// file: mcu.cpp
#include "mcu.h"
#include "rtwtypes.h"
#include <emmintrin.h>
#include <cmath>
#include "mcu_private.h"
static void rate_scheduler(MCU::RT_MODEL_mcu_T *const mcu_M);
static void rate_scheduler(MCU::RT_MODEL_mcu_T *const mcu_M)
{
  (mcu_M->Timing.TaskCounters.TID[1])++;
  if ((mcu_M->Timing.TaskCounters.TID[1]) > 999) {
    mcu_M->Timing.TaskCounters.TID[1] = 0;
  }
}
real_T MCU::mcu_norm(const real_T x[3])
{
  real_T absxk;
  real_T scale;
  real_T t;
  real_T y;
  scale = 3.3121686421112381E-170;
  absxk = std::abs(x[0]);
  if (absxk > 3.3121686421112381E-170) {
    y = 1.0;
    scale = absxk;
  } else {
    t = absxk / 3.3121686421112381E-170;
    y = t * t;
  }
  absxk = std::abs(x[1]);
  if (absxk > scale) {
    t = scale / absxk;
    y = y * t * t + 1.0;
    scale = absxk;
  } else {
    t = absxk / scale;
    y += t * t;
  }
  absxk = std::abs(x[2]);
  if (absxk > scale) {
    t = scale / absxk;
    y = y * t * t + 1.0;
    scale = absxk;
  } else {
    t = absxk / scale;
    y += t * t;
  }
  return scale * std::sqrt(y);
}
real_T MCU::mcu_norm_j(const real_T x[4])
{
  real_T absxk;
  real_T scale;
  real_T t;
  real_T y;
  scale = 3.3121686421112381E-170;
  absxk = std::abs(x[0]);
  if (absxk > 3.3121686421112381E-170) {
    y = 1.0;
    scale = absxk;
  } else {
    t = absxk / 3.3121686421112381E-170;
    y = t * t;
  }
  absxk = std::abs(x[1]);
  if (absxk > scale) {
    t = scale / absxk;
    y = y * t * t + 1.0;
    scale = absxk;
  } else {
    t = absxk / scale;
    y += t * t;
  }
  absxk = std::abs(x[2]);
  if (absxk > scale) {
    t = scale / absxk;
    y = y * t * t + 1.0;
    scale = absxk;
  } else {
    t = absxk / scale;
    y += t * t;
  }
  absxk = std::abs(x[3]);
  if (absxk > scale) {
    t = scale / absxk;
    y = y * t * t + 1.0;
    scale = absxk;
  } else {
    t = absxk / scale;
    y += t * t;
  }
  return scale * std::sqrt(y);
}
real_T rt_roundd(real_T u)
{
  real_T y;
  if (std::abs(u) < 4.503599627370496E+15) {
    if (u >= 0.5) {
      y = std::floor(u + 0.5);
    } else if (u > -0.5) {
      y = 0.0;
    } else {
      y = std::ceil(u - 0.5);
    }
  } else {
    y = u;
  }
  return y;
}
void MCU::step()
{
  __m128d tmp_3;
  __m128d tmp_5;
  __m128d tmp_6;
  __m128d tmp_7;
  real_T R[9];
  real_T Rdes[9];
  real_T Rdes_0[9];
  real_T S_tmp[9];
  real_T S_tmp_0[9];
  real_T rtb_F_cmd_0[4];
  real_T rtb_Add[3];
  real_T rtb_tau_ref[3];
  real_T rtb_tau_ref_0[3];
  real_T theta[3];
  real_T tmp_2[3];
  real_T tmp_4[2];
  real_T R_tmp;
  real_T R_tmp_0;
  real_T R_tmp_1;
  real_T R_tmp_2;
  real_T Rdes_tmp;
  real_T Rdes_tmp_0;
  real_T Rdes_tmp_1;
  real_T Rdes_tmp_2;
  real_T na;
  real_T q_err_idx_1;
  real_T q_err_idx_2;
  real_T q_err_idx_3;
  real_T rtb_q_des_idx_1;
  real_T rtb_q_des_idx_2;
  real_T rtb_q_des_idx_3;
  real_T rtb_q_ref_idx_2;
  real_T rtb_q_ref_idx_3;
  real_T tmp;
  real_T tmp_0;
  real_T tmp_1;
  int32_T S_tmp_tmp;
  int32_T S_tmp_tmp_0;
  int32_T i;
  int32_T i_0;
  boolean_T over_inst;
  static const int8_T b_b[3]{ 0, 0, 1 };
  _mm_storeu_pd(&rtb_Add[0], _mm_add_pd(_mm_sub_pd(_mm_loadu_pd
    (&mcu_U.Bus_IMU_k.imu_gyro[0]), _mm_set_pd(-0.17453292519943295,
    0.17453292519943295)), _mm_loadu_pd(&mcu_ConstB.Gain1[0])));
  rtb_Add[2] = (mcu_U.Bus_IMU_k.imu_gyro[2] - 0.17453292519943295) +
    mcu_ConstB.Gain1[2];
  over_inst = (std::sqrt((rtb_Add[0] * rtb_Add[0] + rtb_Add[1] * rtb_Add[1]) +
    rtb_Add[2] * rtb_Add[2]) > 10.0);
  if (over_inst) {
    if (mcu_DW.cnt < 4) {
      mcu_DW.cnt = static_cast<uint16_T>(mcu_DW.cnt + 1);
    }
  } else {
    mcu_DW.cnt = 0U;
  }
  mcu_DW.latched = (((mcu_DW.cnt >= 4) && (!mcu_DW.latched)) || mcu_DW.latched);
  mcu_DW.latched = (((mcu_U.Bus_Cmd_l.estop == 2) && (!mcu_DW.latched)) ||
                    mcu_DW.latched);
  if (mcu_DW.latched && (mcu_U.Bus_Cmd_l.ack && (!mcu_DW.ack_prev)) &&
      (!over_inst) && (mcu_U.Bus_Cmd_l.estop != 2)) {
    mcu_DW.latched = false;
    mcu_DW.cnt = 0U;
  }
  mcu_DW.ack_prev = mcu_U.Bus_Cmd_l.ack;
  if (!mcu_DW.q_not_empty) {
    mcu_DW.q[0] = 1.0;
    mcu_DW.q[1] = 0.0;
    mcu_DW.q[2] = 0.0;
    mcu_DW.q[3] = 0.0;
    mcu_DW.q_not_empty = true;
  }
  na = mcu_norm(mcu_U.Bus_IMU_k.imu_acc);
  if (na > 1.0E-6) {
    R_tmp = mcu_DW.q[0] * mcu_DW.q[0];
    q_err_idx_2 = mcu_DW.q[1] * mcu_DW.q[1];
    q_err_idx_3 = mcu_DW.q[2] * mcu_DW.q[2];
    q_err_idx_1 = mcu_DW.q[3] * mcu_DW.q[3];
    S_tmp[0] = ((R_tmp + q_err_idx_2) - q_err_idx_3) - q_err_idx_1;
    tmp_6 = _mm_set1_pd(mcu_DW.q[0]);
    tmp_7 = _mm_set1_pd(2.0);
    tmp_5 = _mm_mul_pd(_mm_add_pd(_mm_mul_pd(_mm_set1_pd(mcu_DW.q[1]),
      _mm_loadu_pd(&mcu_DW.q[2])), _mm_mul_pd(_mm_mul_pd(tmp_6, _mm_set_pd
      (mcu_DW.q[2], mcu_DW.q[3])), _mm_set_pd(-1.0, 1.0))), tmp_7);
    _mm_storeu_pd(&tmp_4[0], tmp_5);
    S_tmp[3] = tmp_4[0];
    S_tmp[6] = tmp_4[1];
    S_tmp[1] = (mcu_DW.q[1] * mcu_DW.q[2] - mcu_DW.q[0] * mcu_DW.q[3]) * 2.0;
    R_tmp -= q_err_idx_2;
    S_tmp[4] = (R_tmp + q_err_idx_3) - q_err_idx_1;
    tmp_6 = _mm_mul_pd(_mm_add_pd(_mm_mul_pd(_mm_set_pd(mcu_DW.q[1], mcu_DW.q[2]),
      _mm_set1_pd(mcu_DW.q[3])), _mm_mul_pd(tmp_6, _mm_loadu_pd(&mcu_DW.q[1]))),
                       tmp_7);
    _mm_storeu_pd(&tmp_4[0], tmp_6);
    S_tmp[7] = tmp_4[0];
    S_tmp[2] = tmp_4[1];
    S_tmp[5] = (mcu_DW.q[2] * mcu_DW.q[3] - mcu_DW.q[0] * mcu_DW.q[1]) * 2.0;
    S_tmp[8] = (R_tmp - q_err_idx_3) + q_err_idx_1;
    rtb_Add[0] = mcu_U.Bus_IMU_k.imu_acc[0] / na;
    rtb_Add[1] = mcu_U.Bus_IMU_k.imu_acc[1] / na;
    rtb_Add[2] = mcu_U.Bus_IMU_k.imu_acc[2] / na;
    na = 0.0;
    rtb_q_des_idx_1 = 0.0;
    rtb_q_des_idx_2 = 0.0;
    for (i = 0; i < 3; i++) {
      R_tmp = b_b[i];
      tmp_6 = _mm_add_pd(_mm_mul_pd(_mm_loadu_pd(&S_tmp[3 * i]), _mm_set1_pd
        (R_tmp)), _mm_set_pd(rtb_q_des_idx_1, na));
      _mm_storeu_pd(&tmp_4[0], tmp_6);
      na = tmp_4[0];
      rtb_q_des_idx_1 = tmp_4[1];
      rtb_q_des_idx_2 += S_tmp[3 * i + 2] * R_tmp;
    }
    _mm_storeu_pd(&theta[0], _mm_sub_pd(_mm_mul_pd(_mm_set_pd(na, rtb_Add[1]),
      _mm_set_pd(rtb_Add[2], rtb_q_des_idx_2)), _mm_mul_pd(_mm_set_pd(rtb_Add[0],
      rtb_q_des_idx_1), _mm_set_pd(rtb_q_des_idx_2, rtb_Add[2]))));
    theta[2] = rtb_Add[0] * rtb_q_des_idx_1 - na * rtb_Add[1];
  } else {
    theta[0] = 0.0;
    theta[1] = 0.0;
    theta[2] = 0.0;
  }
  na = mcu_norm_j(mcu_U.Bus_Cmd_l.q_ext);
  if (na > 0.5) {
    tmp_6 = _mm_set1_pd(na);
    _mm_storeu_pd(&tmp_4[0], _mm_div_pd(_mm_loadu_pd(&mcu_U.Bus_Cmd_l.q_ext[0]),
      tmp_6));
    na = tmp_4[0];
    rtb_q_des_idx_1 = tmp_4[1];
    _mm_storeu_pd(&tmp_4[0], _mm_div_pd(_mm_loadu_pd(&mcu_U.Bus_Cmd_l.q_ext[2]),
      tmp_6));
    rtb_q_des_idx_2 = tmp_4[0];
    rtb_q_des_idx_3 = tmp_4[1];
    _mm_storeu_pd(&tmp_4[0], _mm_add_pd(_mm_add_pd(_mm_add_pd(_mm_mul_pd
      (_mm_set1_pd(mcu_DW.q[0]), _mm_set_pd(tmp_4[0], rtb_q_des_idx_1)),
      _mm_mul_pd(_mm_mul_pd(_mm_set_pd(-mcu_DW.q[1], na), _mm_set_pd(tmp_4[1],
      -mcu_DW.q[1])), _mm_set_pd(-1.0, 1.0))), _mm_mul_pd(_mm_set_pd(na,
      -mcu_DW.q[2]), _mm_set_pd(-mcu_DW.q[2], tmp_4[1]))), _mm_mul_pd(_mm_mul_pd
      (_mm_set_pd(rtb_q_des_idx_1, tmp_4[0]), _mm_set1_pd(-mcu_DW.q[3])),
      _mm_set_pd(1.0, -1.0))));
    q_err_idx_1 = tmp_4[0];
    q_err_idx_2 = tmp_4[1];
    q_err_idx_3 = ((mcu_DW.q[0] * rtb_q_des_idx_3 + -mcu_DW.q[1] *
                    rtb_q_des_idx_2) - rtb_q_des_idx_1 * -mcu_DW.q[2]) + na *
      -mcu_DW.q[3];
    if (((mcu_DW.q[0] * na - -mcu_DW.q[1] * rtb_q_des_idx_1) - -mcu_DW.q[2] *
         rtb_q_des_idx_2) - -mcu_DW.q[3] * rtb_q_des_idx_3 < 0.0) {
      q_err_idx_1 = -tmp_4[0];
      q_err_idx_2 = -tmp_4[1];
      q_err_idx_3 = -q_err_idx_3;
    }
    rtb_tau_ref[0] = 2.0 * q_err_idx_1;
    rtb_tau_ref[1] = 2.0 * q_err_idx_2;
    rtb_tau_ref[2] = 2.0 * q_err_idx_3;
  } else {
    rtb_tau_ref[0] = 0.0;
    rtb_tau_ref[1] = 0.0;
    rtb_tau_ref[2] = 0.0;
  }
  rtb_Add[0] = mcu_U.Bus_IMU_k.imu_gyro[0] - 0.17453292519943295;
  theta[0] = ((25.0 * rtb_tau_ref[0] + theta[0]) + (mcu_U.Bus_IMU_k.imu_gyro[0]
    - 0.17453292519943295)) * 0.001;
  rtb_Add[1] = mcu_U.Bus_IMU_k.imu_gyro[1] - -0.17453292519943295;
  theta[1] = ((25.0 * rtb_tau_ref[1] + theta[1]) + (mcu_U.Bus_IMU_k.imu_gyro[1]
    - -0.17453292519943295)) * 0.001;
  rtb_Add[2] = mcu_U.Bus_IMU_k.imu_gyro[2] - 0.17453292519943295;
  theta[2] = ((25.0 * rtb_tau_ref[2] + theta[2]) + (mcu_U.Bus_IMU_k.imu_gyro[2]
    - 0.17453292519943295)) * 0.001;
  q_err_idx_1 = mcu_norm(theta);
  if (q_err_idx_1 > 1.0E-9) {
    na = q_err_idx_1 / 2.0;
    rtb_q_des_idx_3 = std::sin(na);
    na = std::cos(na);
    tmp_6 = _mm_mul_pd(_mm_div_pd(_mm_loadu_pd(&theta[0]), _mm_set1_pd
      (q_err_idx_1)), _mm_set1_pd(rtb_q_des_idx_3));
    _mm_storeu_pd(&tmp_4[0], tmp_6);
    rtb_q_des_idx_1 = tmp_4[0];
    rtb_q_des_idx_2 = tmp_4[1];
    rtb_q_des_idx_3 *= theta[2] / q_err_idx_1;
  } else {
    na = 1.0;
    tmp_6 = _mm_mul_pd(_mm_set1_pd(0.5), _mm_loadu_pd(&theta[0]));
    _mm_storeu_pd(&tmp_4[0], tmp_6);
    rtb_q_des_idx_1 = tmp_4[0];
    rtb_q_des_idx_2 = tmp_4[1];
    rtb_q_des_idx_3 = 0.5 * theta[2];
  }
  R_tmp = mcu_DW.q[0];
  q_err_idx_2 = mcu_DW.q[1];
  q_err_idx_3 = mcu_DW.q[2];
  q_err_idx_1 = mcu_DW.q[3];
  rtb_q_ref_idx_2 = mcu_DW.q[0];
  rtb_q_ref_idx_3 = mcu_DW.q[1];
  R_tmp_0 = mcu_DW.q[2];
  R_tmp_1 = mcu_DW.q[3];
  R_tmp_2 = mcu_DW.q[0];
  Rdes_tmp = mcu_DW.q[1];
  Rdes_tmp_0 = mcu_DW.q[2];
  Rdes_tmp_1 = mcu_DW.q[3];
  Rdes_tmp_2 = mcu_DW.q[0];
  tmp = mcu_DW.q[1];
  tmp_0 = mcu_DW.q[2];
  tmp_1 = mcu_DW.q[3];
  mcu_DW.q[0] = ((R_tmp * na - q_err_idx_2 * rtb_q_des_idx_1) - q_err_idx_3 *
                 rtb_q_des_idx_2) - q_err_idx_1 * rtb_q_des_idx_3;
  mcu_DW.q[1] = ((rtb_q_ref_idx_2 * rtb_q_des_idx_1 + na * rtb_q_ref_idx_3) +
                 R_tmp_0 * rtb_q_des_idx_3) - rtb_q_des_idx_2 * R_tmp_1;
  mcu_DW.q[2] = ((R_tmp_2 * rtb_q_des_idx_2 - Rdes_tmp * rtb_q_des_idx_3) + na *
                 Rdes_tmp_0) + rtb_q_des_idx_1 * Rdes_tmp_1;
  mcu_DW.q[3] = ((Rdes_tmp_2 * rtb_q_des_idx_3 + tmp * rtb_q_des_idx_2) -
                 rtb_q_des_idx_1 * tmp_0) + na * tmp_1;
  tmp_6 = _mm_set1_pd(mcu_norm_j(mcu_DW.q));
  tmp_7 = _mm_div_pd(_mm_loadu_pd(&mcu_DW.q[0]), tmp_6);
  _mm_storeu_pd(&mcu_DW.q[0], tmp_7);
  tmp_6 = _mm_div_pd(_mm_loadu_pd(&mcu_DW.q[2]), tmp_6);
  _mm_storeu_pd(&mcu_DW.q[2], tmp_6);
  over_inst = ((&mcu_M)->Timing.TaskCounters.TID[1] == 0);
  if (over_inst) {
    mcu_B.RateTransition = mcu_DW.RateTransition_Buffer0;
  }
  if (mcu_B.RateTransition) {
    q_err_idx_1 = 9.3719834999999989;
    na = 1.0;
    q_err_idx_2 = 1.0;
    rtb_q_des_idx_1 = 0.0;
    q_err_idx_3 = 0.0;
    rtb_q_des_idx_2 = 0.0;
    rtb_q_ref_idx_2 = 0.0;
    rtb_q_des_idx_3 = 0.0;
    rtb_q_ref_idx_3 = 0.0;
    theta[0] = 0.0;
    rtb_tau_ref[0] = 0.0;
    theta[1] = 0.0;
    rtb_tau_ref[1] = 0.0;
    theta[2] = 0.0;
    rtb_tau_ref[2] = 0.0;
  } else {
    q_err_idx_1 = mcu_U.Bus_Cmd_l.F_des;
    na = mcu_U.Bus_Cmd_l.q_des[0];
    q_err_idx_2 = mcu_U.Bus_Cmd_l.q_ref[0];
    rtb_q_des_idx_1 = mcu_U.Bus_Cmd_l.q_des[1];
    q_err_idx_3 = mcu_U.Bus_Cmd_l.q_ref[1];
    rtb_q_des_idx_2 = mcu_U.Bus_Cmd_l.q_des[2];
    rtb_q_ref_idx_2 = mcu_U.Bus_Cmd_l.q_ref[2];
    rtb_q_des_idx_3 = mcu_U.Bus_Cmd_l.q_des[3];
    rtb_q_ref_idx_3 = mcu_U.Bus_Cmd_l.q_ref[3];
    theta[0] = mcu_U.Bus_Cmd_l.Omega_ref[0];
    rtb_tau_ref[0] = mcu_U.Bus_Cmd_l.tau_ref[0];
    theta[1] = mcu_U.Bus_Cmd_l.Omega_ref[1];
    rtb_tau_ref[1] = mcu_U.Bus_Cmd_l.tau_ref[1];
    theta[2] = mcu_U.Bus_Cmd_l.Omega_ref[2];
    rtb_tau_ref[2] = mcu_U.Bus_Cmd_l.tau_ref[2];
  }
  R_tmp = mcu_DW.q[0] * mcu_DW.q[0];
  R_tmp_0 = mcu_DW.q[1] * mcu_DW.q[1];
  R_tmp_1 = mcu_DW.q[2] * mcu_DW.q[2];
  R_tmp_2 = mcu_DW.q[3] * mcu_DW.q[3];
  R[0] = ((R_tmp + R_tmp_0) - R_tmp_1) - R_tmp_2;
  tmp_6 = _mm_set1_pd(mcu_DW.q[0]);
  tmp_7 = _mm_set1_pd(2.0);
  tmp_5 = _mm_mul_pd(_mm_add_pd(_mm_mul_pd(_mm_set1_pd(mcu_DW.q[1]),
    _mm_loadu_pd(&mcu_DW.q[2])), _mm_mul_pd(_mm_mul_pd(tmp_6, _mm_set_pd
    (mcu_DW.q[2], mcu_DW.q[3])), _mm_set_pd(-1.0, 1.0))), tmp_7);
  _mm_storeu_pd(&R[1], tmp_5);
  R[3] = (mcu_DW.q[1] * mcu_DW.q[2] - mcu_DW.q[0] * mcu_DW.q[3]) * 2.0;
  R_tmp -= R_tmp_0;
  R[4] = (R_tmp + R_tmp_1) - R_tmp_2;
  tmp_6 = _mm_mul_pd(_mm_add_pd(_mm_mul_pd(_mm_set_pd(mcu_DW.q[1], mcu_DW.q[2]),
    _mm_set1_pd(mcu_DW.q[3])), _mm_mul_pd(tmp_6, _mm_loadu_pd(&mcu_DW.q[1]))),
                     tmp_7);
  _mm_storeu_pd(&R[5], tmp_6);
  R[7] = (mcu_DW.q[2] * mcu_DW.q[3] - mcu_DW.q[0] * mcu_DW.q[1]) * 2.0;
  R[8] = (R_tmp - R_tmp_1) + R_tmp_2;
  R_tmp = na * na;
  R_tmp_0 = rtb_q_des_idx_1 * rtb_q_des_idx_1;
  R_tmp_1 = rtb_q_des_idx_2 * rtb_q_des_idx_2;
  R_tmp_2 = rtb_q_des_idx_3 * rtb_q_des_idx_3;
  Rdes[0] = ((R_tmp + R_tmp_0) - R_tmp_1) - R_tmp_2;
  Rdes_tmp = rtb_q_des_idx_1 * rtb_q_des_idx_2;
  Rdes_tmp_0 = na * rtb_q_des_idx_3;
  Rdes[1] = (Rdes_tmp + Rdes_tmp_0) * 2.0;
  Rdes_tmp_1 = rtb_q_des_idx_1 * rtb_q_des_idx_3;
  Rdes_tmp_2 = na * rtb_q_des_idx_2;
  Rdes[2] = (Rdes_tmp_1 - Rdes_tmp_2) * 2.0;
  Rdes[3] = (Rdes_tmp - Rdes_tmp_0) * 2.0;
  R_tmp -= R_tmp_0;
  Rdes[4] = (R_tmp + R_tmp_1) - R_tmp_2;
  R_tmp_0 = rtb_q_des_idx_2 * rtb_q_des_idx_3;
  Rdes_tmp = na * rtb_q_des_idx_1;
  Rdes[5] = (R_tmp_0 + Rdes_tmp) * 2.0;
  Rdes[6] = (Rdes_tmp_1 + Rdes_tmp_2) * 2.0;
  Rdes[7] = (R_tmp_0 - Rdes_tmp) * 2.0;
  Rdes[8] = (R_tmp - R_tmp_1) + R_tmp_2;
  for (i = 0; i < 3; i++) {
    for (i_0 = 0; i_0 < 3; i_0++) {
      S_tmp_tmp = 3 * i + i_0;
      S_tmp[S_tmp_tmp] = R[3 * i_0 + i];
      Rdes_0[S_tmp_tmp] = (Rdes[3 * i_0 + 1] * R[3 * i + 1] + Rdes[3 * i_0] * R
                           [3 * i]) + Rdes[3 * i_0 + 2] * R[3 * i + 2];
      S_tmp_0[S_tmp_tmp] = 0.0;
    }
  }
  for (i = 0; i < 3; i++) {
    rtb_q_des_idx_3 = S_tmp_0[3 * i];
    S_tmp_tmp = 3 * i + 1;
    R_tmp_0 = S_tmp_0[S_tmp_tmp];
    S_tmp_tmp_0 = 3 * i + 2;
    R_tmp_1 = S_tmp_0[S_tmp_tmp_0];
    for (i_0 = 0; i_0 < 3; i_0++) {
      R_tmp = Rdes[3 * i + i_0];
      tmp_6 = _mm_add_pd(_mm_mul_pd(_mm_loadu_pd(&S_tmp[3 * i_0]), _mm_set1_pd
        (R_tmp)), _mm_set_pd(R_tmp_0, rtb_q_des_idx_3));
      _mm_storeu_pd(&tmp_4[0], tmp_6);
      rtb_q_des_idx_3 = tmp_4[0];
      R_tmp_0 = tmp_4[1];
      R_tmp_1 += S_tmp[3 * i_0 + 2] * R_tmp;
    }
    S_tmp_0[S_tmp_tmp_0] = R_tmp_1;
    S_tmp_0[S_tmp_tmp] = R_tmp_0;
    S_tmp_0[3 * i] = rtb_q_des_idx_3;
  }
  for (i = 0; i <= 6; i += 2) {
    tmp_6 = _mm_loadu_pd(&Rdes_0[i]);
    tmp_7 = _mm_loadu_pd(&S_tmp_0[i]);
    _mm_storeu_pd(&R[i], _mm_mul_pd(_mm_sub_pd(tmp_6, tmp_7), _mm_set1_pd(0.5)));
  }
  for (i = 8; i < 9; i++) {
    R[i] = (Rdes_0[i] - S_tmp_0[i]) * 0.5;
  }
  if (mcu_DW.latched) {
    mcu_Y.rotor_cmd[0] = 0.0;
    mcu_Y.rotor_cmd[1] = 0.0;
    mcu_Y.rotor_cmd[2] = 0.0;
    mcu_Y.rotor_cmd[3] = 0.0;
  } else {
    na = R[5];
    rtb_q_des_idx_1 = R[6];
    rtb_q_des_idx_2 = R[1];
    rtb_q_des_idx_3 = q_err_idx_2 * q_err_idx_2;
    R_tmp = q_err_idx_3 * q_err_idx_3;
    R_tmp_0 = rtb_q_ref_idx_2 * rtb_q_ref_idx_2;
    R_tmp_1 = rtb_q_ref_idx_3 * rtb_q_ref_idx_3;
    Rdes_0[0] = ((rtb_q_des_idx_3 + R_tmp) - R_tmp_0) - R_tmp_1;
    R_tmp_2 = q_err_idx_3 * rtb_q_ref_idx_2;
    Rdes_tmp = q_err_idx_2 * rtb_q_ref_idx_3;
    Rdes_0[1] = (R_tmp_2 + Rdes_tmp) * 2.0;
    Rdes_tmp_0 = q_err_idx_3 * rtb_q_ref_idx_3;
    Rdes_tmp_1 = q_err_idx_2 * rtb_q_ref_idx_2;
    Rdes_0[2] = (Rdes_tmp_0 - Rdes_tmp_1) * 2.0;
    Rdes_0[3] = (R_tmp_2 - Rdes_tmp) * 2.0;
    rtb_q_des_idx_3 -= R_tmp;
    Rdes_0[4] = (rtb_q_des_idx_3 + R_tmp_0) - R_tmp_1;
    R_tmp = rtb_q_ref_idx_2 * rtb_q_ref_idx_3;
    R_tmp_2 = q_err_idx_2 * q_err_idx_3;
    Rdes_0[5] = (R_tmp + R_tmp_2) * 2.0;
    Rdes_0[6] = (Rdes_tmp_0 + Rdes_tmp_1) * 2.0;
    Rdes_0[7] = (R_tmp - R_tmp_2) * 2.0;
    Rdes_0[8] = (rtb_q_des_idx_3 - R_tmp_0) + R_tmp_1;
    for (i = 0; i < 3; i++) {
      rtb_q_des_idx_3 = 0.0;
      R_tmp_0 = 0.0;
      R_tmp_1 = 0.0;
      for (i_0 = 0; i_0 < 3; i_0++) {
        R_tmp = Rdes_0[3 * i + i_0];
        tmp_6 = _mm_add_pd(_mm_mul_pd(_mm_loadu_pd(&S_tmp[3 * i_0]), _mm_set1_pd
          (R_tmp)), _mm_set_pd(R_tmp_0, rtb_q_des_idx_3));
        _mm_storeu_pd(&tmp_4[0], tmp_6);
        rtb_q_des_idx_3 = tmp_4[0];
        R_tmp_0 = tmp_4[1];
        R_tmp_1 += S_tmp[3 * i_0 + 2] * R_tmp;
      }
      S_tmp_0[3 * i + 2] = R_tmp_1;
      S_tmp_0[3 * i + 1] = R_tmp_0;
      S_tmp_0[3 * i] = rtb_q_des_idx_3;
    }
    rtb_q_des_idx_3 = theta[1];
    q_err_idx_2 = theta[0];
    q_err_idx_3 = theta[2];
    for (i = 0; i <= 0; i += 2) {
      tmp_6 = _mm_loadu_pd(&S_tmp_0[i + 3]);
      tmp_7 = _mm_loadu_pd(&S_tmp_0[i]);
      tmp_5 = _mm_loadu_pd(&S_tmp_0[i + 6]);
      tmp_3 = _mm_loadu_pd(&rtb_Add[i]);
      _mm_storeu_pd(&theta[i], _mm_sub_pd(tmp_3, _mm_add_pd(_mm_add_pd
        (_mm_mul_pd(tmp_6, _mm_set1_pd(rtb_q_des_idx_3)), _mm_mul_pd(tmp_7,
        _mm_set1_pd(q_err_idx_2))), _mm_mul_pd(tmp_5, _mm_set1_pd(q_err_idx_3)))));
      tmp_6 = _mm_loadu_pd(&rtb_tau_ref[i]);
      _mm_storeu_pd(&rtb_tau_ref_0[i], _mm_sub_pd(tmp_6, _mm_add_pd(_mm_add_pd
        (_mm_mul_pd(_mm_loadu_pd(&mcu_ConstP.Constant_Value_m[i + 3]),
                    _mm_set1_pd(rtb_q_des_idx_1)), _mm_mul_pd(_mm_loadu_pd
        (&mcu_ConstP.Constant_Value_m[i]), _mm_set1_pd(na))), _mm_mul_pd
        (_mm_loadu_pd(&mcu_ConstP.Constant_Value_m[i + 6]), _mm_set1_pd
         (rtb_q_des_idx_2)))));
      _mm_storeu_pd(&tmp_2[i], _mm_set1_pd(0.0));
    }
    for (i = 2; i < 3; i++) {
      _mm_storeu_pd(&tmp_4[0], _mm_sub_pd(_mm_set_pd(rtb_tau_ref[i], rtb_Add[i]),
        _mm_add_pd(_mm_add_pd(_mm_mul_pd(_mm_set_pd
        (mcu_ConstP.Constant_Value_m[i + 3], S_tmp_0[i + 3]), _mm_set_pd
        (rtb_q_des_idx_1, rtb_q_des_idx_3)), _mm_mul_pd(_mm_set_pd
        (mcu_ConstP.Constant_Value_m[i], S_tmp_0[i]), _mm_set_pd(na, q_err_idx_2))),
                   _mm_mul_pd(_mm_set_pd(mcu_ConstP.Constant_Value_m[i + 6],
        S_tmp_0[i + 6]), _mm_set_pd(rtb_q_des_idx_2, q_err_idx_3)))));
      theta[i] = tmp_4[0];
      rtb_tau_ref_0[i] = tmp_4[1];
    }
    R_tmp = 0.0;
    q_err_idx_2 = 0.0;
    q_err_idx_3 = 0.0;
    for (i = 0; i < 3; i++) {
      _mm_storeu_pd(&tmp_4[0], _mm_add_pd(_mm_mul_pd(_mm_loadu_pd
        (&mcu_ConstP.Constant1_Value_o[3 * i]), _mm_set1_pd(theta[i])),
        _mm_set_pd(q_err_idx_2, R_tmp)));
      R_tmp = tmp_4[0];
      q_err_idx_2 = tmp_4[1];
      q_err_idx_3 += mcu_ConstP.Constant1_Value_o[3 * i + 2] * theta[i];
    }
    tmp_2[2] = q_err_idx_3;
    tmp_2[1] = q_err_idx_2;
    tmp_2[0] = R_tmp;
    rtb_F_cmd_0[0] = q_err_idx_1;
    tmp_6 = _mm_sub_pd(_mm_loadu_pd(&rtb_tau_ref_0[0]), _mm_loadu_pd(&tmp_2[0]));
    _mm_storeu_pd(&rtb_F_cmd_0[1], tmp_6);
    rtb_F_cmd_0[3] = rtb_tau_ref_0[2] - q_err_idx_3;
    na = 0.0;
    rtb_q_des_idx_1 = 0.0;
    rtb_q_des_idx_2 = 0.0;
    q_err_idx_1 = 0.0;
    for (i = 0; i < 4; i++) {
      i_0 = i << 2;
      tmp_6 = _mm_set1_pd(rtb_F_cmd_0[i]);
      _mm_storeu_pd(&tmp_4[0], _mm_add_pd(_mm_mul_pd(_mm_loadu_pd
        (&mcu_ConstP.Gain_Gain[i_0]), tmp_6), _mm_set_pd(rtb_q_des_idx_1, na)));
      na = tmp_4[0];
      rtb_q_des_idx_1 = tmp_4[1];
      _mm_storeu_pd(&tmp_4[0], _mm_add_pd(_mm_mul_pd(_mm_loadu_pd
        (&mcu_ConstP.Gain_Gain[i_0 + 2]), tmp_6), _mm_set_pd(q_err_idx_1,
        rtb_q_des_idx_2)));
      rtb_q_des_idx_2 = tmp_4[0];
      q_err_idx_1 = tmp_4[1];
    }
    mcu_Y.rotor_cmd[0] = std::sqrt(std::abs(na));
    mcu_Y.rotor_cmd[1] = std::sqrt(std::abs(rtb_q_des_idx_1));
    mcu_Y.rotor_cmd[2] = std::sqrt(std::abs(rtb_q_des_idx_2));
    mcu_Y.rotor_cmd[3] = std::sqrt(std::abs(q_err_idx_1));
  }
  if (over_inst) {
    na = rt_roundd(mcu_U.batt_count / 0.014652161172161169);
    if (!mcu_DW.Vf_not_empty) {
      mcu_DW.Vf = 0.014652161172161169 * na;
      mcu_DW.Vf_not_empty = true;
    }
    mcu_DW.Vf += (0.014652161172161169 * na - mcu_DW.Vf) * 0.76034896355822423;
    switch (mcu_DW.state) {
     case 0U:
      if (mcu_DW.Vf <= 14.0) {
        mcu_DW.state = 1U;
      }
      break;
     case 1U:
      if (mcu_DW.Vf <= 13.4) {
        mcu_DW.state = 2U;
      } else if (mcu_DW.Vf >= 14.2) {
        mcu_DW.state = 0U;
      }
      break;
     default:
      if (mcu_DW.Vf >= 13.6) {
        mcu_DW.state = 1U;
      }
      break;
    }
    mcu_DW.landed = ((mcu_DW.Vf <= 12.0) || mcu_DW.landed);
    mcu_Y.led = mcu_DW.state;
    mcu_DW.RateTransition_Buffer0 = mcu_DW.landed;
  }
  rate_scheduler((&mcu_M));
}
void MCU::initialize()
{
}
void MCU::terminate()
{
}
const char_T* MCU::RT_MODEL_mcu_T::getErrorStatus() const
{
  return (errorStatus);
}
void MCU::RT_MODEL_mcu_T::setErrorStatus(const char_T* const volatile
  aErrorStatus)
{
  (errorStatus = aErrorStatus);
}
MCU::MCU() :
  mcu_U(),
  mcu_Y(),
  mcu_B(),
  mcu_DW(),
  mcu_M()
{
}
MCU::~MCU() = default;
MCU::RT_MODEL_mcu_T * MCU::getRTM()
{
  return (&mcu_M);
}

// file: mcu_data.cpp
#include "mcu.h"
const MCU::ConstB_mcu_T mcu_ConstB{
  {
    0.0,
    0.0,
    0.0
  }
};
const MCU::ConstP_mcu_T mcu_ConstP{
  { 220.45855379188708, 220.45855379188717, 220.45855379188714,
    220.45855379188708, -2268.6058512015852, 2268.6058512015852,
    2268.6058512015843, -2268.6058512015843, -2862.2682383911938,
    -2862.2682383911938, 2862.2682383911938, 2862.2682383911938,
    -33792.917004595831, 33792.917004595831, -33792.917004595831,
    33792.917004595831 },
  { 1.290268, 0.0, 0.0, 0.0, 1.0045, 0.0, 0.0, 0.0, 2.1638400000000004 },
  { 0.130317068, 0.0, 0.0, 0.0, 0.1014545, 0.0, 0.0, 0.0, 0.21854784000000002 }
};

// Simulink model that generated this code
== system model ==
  Bus_IMU : Inport
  Bus_Cmd : Inport
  batt_count : Inport
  rotor_cmd : Outport  <- 1: Switch#1
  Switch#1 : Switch  Criteria=u2 > Threshold  <- 1: Constant#1, 2: MATLABFunction#1, 3: Sqrt#1
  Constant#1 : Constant  Value=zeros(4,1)
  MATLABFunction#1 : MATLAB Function  <- 1: Add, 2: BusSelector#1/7, 3: Logic#1
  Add : Sum  <- 1: Sum#1, 2: Gain1
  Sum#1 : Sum  Inputs=+-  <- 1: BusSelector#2, 2: Constant1
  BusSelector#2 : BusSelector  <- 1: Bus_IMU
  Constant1 : Constant  Value=imu.gyro_bias
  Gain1 : Gain  Gain=0  <- 1: Constant#2
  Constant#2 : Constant  Value=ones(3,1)
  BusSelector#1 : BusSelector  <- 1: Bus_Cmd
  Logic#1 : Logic  Operator=OR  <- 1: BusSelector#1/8, 2: Constant#3
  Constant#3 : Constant  Value=0
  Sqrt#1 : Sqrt  <- 1: Abs#1
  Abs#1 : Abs  <- 1: Gain
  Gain : Gain  Gain=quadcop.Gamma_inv  Multiplication=Matrix(K*u) (u vector)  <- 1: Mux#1
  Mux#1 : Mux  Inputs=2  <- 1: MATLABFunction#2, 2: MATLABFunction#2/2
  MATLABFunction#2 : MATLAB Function  <- 1: MATLABFunction#3, 2: MATLABFunction#3/2, 3: MATLABFunction#4, 4: MATLABFunction#4/5, 5: MATLABFunction#4/2, 6: MATLABFunction#4/3, 7: MATLABFunction#4/4, 8: Constant, 9: Constant#4
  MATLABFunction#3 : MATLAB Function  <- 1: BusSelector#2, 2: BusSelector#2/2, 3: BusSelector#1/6, 4: Constant#5, 5: Constant#6, 6: Constant#7, 7: Constant#8, 8: Constant1
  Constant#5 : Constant  Value=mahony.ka
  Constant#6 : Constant  Value=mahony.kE
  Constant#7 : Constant  Value=imu.Ts
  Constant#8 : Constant  Value=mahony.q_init
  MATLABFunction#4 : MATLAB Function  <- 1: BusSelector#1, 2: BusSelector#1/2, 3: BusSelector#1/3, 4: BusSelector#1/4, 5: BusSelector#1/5, 6: RateTransition
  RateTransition : RateTransition  <- 1: MATLABFunction#5/2
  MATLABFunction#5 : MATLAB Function  <- 1: MATLABFunction#6
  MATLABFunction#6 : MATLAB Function  <- 1: batt_count
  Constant : Constant  Value=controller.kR
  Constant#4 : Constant  Value=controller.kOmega
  led : Outport  <- 1: MATLABFunction#5
== matlab function MATLAB Function ==
function [F, tau] = geo_attitude_ctrl(q, Omega, q_des, q_ref, Omega_ref, F_des, tau_ref, kR, kOmega)
%#codegen
% GEO_ATTITUDE_CTRL Geometrischer Lageregler auf SO(3).
%   Lee/Leok/McClamroch (CDC 2010), 2-DOF Error-Feedback:
%       tau = tau_ff - kR*eR - kOmega*eOmega
%
%   ZWEI getrennte Referenzen (NICHT identisch!):
%     q_des : Solllage aus dem Folgeregler pos_ctrl (mit Positionsrueckfuehrung)
%             -> bestimmt den Lagefehler e_R.
%     q_ref : nominelle Solllage aus traj_gen (reine Vorsteuerung)
%             -> Frame, in dem Omega_ref definiert ist ([Om_ref]x = R_ref' R^T_ref)
%             -> Transport von Omega_ref in den aktuellen Body-Frame.
%
%
%   EIN-/AUSGAENGE:
%     q, Omega         : aktuelle Lage/Drehrate
%     q_des            : Solllage aus pos_ctrl
%     q_ref            : Solllage aus traj_gen 
%     Omega_ref        : Vorsteuer-Drehrate im Body-Frame aus traj_gen
%     F_des, tau_ff    : Vorsteuerung Schub/Moment aus traj_gen
%     kR, kOmega       : 3x3-Gains
%     F, tau           : Schubsollwert, Stellmoment

R    = quat2dcm_local(q)';      
Rdes = quat2dcm_local(q_des)';   
Rref = quat2dcm_local(q_ref)';    

% --- Lagefehler gegen die rueckgefuehrte Solllage R_des ---
S  = 0.5*(Rdes'*R - R'*Rdes);     % schiefsymmetrisch
eR = [S(3,2); S(1,3); S(2,1)];    % vee

% --- Drehratenfehler: Omega_ref aus R_ref-Frame in aktuellen Frame transportieren ---
eOmega = Omega - R'*Rref*Omega_ref;

% --- Stellgesetz ---
tau = tau_ref - kR*eR - kOmega*eOmega;
% Optional voll-geometrisch: 
% tau = tau + cross(Omega, J*Omega);

F = F_des;
end

== matlab function MATLAB Function ==
function [q_hat, Omega_hat] = mahony_filter(imu_gyro, imu_acc, q_ext, ka, kE, Ts, q_init, b_ground)
%#codegen
% MAHONY_FILTER  Expliziter Komplementaerfilter auf SO(3), zeitdiskret.
%   Mahony/Hamel/Pflimlin (TAC 2008)). km = 0 (kein Magnetometer)
%
%     - Accel misst spezifische Kraft; im Hover [0;0;-g] -> Richtung
%       v0 = [0;0;-1]. 
%
%   EIN-/AUSGAENGE:
%     imu_gyro [rad/s] (3x1)  : gemessene Koerperdrehrate (mit Bias+Rauschen)
%     imu_acc  [m/s^2] (3x1)  : gemessene spezifische Kraft (Koerper)
%     q_ext    (4x1)          : externe Mocap-Lage 
%     ka, kE, kb (Skalar)     : Tilt-, Externreferenz-, Bias-Gain
%     Ts       [s]            : Abtastperiode 
%     q_init   (4x1)          : Startlage 
%     b_init   (3x1)          : Startbias
%     b_clamp  (Skalar)       : Maximalwert des Bias
%     q_hat    (4x1)          : geschaetzte Lage
%     Omega_hat(3x1)          : bias-korrigierte Drehrate (fuer Lageregler)
%     b_hat    (3x1)          : geschaetzter Gyro-Bias (Diagnose)
%     e_acc    (3x1)          : Innovationsterm zur Diagnose

persistent q
if isempty(q)
    q = q_init; % Startlage
end

% --- 1) Innovation (nur Richtung, Betrag traegt keine Lageinfo) ---
na = norm(imu_acc);
if na > 1e-6
    v_acc = imu_acc / na; % spezifische Kraft DCM_{be}(a -g*[0;0;-1]) in Körperkoordinaten
    v_hat = quatRotate(q, [0; 0; 1]); % geschaetzte Schwerkraftrichtung in Körperkoordinaten
    e_acc = cross(v_acc, v_hat); % Schätzfehler = Innovationsterm
else
    e_acc = [0; 0; 0]; % Freifall = unbrauchbar
end

% --- 2) Externe Mocap-Lage ---
nE = norm(q_ext);
if nE > 0.5
    qe    = q_ext / nE; % normieren da durch Quantisierung/Rauschen q_ext kein Einheitsquaternion
    q_err = quatMul(quatConj(q), qe); % Koerperinkrement, das \hat{q} -> q_ext dreht
    if q_err(1) < 0 
        q_err = -q_err; % kuerzeste Drehung, da Doppeldeckung des SO(3) durch Quaternionen
    end  
    e_ext = 2 * q_err(2:4); % Rotationsvektor (Kleinwinkel ~ Fehlerwinkel)
else
    e_ext = [0; 0; 0]; % kein gueltiges q_ext -> für Innovationsterm nur Gyro und Accel nutzen
end

% --- 3) Gewichtete Gesamt-Innovation (Koerperframe) ---
omega_mes = ka * e_acc + kE * e_ext;

% --- 5) Korrigierte Drehrate + Quaternion-Propagation ---
omega = imu_gyro - b_ground + omega_mes; % Eingang der Kinematik
theta = omega * Ts;
ang   = norm(theta);
if ang > 1e-9
    norm_theta = theta / ang;
    dq = [cos(ang/2); sin(ang/2) * norm_theta];
else
    dq = [1; 0.5 * theta]; % Kleinwinkel-Naeherung
end
q = quatMul(q, dq); % Rechtsmultiplikation = Koerperinkrement
q = q / norm(q); % auf SO(3) halten

% --- 6) Ausgaenge ---
q_hat     = q;
Omega_hat = imu_gyro - b_ground; % Bias-korrigiert
end

== matlab function MATLAB Function ==
function [kill, fault_src, dbg] = safety_overspeed(gyro_corr, estop, ack, safety)
%#codegen
% SAFETY_OVERSPEED  Onboard-KILL-Latch
%
% Overspeed-Entprell-Latch ∪ Hard-Kill (estop==2).
% Aktion downstream: rotors_cmd = 0  (Override NACH Mixer / VOR Motor-PT1+ESC).
% KILL dominiert LAND; KILL latcht; Re-Arm NIE in der Luft.
%
% Warum eine Funktion fuer beide KILL-Quellen: Overspeed und Hard-Kill teilen
% denselben Latch, dieselbe Aktion (rotors_cmd=0) und dieselbe Re-Arm-Semantik
% (ack loescht). Eine gemeinsame Funktion haelt die Re-Arm-Bedingung an EINER
% Stelle und macht "KILL dominiert LAND" trivial. Der geregelte Soft-Land
% (estop==1) wird hier NICHT behandelt — das ist die GCS-Mode-Maschine.
%
% Eingaenge
%   gyro_corr : 3x1  bias-korrigierte Drehrate [rad/s]  (MESSUNG, nicht Schaetzer!)
%   estop : uint8  0 normal / 1 soft-land / 2 hard-kill (aus Bus_Cmd, Uplink)
%   ack : bool   Quittung, bereits ge-OR-t (Teensy-Taster-Flanke | Bus_Cmd.ack)
%   safety : struct  .omega_max [rad/s], .debounce_N (>=1), .use_norm (bool)
%
% Ausgaenge
%   kill : bool   latched -> nachgelagerter Switch zwingt rotors_cmd=0
%   fault_src : uint8  0 none / 1 overspeed / 2 hard-kill   (LED/Debug)
%   dbg : 3x1    [cnt; over_inst; ack_edge]           (verify/logging)
%
% Re-Arm (FAULT->ARMED) NUR bei:  steigende ack-Flanke  &  ~over_inst  &  estop~=2.
% Die ack-FLANKE (nicht der Pegel) verhindert, dass ein gehaltenes ack einen
% frischen Trip sofort wieder loescht oder mid-air in einen Sturz re-armt. Die
% Boden-Bedingung ("nie in der Luft") wird prozedural durch den physischen
% Teensy-Taster garantiert (Bediener hebt die Drohne auf, drueckt) — onboard
% existiert keine Pos/Vel-Schaetzung fuer ein Logik-Interlock (sitzt GCS-seitig).
% Optionaler Idle-Interlock siehe Hinweis am Dateiende.

persistent latched cnt ack_prev src
if isempty(latched)
    latched = false;
    cnt = uint16(0);
    ack_prev = false;
    src = uint8(0);
end

gw = reshape(gyro_corr, 3, 1);

% --- Overspeed-Detektor, entprellt (N aufeinanderfolgende Samples) ---
if safety.use_norm
    over_inst = sqrt(gw(1)*gw(1) + gw(2)*gw(2) + gw(3)*gw(3)) > safety.omega_max;
else
    over_inst = (abs(gw(1)) > safety.omega_max) || ...
                (abs(gw(2)) > safety.omega_max) || ...
                (abs(gw(3)) > safety.omega_max);
end

Nreq = uint16(safety.debounce_N);
if over_inst
    if cnt < Nreq
        cnt = cnt + uint16(1);
    end
else
    cnt = uint16(0);                 % ein gutes Sample setzt den Zaehler zurueck
end
over_deb = cnt >= Nreq;

% --- Hard-Kill: sofort, keine Entprellung ---
hard_kill = (estop == uint8(2));

% --- KILL setzen (latcht; Quelle nur beim ersten Setzen vermerkt) ---
if over_deb && ~latched
    latched = true;  
    src = uint8(1); % due to fast turning rates from gyro
end
if hard_kill && ~latched
    latched = true;  
    src = uint8(2);
end

% Re-Arm: steigende ack-Flanke 
ack_edge = ack && ~ack_prev;
if latched && ack_edge && ~over_inst && (estop ~= uint8(2)) % momentan kein Overspeed & kein Hard-Kill
    latched = false;
    cnt     = uint16(0);
    src     = uint8(0);
end
ack_prev = ack;

kill      = latched;
fault_src = src;
dbg       = [double(cnt); double(over_inst); double(ack_edge)];
end

% -------------------------------------------------------------------------
% OPTIONALER IDLE-INTERLOCK (nicht aktiviert):
% Will man re-arm zusaetzlich gegen "in der Luft" absichern OHNE Pos-Schaetzung,
% kann onboard ein Throttle-Idle-Proxy gefordert werden, z.B. F_ref <= F_idle:
%   ...&& (F_ref <= safety.F_rearm_idle) ...
% F_ref liegt im empfangenen Bus_Cmd vor. Das ersetzt die Boden-Schaetzung durch
% "Bediener hat heruntergeregelt", bleibt aber Heuristik (Hover braucht m*g>0).
% Bewusst NICHT verdrahtet, bis §13 das fordert.

== matlab function MATLABFunction#5 ==
function [led, batt_land, V_filt] = safety_battery(batt_count, safety)
%#codegen
% safety_battery Onboard-Batterie-Monitor, 4S LiPo via PM06 V2.
%
% Kette: ADC-count --> V_batt --> V_filt --> led
%        V_filt <= V_floor --(Latch bis Reboot) --> batt_land
%
%   WARN/CRIT -> LED. Bediener im Raum sieht sie, loest MANUELL GCS-Soft-Land
%               (estop=1 => Uplink) aus, solange Marge da ist.
%   FLOOR     -> batt_land = true -> onboard BLINDER Hard-Floor-Descent 
%               (safety_landcmd.m) als Backstop, falls niemand reagiert.
% KILL (Overspeed/Hard-Kill) dominiert: rotors_cmd=0 nachgelagert sticht jeden LAND.
%
% LATCH IST PERMANENT —> KEIN Re-Arm. Zwei Gruende:
%   1) Akkuwechsel = Teensy-Reboot -> persistent wird genullt.
%   2) WICHTIGER: Im Descent faellt der Schub auf 0.98*m*g -> weniger Strom ->
%      V erholt sich UEBER den Floor. Ohne Latch wuerde batt_land deasserten,
%      das GCS-Kommando (Hover @ m*g) kaeme zurueck, Last steigt, V sackt wieder
%      -> GRENZZYKLUS Sinken<->Schweben auf fast leerem Akku. Der Latch verhindert
%      das: einmal committed -> bis zum Boden sinken.
%
% Eingaenge:
%   batt_count : ADC-Rohwert (12 bit, 0..4095). In Sim aus simulierter V-Rampe
%                (count = round((V_batt - b)/k)); auf HW analogRead(A16/Pin40).
%   safety     : struct  .batt_k .batt_b .batt_alpha .V_warn .V_crit .V_floor
%                        .V_hyst
% Ausgaenge:
%   led        : uint8  0 NORMAL / 1 WARN / 2 CRIT   (-> GPIO-Blinkmuster)
%   batt_land  : bool   latched -> safety_landcmd Hard-Floor-Override
%   V_filt     : double gefilterte Batteriespannung [V]  (dbg/logging)
%
% Hysterese: Recovery (Richtung NORMAL) braucht + V_hyst -> kein Flattern bei
% Last-Sag/Rauschen. (tau ~0.5..1 s) glaettet Sag + Rauschen UND verhindert,
% dass ein kurzer Spannungseinbruch unter Last den Floor faelschlich triggert.

persistent Vf state landed
if isempty(Vf)
    Vf     = safety.batt_k * double(batt_count) + safety.batt_b;  % init
    state  = uint8(0);
    landed = false;
end

% --- ADC -> Spannung ---
V_raw = safety.batt_k * double(batt_count) + safety.batt_b;

% --- Tiefpass: V_filt += alpha*(V_raw - V_filt) ---
Vf = Vf + safety.batt_alpha * (V_raw - Vf);
V  = Vf;

% --- 3-stufige LED mit Hysterese (Batterienzeige) ---
% NORMAL(0) -> WARN(1) -> CRIT(2); Rueckweg braucht + V_hyst.
switch state
    case uint8(0) % NORMAL
        if V <= safety.V_warn                     
            state = uint8(1); 
        end
    case uint8(1) % WARN
        if V <= safety.V_crit                 
            state = uint8(2);
        elseif V >= safety.V_warn + safety.V_hyst
            state = uint8(0); 
        end
    otherwise % CRIT (2)
        if V >= safety.V_crit + safety.V_hyst     
            state = uint8(1); 
        end
end

% --- harte Landung ---
if V <= safety.V_floor
    landed = true;
end

led       = state;
batt_land = landed;
V_filt    = V;
end

== matlab function MATLABFunction#6 ==
function count = v2c(v, safety)

count = round((v - safety.batt_b)/safety.batt_k);

== matlab function MATLABFunction#4 ==
function [q_des, Omega_ref, F_cmd, tau_ref, q_ref] = ...
         safety_landcmd(F_in, q_des_in, q_ref_in, Omega_ref_in, tau_ref_in, ...
                        batt_land, safety)
%#codegen
% SAFETY_LANDCMD  Onboard BLINDE harte Landung
%
% Sitzt im Pfad VOR geo_attitude_ctrl. Bei batt_land = true ueberschreibt
% er den empfangenen Kommandosatz durch einen blinden Sinkflug.
% BLIND, weil onboard KEINE Pos/Vel-Schaetzung existiert. 
%
% Eingaenge: 
%   F_in         : scalar  Schub-Kommando an geo_attitude_ctrl (F = F_des)
%   q_des_in     : 4x1     Folgeregler-Lage (pos_ctrl)
%   q_ref_in     : 4x1     Vorsteuerlage (traj_gen)
%   Omega_ref_in : 3x1     Vorsteuer-Rate
%   tau_ref_in   : 3x1     Vorsteuer-Moment
%   batt_land    : bool    aus safety_battery 
%   safety       : struct  .m .g .hardfloor_thrust_frac 
% Ausgaenge an geo_attitude_ctrl.

    if batt_land
        F_cmd     = safety.hardfloor_thrust_frac * safety.m * safety.g;  % < m*g
        q_des     = [1; 0; 0; 0];     
        q_ref     = [1; 0; 0; 0];
        Omega_ref = [0; 0; 0];
        tau_ref   = [0; 0; 0];
    else
        F_cmd     = F_in;
        q_des = q_des_in;
        q_ref = q_ref_in;
        Omega_ref = Omega_ref_in;
        tau_ref = tau_ref_in;
    
    end
end
